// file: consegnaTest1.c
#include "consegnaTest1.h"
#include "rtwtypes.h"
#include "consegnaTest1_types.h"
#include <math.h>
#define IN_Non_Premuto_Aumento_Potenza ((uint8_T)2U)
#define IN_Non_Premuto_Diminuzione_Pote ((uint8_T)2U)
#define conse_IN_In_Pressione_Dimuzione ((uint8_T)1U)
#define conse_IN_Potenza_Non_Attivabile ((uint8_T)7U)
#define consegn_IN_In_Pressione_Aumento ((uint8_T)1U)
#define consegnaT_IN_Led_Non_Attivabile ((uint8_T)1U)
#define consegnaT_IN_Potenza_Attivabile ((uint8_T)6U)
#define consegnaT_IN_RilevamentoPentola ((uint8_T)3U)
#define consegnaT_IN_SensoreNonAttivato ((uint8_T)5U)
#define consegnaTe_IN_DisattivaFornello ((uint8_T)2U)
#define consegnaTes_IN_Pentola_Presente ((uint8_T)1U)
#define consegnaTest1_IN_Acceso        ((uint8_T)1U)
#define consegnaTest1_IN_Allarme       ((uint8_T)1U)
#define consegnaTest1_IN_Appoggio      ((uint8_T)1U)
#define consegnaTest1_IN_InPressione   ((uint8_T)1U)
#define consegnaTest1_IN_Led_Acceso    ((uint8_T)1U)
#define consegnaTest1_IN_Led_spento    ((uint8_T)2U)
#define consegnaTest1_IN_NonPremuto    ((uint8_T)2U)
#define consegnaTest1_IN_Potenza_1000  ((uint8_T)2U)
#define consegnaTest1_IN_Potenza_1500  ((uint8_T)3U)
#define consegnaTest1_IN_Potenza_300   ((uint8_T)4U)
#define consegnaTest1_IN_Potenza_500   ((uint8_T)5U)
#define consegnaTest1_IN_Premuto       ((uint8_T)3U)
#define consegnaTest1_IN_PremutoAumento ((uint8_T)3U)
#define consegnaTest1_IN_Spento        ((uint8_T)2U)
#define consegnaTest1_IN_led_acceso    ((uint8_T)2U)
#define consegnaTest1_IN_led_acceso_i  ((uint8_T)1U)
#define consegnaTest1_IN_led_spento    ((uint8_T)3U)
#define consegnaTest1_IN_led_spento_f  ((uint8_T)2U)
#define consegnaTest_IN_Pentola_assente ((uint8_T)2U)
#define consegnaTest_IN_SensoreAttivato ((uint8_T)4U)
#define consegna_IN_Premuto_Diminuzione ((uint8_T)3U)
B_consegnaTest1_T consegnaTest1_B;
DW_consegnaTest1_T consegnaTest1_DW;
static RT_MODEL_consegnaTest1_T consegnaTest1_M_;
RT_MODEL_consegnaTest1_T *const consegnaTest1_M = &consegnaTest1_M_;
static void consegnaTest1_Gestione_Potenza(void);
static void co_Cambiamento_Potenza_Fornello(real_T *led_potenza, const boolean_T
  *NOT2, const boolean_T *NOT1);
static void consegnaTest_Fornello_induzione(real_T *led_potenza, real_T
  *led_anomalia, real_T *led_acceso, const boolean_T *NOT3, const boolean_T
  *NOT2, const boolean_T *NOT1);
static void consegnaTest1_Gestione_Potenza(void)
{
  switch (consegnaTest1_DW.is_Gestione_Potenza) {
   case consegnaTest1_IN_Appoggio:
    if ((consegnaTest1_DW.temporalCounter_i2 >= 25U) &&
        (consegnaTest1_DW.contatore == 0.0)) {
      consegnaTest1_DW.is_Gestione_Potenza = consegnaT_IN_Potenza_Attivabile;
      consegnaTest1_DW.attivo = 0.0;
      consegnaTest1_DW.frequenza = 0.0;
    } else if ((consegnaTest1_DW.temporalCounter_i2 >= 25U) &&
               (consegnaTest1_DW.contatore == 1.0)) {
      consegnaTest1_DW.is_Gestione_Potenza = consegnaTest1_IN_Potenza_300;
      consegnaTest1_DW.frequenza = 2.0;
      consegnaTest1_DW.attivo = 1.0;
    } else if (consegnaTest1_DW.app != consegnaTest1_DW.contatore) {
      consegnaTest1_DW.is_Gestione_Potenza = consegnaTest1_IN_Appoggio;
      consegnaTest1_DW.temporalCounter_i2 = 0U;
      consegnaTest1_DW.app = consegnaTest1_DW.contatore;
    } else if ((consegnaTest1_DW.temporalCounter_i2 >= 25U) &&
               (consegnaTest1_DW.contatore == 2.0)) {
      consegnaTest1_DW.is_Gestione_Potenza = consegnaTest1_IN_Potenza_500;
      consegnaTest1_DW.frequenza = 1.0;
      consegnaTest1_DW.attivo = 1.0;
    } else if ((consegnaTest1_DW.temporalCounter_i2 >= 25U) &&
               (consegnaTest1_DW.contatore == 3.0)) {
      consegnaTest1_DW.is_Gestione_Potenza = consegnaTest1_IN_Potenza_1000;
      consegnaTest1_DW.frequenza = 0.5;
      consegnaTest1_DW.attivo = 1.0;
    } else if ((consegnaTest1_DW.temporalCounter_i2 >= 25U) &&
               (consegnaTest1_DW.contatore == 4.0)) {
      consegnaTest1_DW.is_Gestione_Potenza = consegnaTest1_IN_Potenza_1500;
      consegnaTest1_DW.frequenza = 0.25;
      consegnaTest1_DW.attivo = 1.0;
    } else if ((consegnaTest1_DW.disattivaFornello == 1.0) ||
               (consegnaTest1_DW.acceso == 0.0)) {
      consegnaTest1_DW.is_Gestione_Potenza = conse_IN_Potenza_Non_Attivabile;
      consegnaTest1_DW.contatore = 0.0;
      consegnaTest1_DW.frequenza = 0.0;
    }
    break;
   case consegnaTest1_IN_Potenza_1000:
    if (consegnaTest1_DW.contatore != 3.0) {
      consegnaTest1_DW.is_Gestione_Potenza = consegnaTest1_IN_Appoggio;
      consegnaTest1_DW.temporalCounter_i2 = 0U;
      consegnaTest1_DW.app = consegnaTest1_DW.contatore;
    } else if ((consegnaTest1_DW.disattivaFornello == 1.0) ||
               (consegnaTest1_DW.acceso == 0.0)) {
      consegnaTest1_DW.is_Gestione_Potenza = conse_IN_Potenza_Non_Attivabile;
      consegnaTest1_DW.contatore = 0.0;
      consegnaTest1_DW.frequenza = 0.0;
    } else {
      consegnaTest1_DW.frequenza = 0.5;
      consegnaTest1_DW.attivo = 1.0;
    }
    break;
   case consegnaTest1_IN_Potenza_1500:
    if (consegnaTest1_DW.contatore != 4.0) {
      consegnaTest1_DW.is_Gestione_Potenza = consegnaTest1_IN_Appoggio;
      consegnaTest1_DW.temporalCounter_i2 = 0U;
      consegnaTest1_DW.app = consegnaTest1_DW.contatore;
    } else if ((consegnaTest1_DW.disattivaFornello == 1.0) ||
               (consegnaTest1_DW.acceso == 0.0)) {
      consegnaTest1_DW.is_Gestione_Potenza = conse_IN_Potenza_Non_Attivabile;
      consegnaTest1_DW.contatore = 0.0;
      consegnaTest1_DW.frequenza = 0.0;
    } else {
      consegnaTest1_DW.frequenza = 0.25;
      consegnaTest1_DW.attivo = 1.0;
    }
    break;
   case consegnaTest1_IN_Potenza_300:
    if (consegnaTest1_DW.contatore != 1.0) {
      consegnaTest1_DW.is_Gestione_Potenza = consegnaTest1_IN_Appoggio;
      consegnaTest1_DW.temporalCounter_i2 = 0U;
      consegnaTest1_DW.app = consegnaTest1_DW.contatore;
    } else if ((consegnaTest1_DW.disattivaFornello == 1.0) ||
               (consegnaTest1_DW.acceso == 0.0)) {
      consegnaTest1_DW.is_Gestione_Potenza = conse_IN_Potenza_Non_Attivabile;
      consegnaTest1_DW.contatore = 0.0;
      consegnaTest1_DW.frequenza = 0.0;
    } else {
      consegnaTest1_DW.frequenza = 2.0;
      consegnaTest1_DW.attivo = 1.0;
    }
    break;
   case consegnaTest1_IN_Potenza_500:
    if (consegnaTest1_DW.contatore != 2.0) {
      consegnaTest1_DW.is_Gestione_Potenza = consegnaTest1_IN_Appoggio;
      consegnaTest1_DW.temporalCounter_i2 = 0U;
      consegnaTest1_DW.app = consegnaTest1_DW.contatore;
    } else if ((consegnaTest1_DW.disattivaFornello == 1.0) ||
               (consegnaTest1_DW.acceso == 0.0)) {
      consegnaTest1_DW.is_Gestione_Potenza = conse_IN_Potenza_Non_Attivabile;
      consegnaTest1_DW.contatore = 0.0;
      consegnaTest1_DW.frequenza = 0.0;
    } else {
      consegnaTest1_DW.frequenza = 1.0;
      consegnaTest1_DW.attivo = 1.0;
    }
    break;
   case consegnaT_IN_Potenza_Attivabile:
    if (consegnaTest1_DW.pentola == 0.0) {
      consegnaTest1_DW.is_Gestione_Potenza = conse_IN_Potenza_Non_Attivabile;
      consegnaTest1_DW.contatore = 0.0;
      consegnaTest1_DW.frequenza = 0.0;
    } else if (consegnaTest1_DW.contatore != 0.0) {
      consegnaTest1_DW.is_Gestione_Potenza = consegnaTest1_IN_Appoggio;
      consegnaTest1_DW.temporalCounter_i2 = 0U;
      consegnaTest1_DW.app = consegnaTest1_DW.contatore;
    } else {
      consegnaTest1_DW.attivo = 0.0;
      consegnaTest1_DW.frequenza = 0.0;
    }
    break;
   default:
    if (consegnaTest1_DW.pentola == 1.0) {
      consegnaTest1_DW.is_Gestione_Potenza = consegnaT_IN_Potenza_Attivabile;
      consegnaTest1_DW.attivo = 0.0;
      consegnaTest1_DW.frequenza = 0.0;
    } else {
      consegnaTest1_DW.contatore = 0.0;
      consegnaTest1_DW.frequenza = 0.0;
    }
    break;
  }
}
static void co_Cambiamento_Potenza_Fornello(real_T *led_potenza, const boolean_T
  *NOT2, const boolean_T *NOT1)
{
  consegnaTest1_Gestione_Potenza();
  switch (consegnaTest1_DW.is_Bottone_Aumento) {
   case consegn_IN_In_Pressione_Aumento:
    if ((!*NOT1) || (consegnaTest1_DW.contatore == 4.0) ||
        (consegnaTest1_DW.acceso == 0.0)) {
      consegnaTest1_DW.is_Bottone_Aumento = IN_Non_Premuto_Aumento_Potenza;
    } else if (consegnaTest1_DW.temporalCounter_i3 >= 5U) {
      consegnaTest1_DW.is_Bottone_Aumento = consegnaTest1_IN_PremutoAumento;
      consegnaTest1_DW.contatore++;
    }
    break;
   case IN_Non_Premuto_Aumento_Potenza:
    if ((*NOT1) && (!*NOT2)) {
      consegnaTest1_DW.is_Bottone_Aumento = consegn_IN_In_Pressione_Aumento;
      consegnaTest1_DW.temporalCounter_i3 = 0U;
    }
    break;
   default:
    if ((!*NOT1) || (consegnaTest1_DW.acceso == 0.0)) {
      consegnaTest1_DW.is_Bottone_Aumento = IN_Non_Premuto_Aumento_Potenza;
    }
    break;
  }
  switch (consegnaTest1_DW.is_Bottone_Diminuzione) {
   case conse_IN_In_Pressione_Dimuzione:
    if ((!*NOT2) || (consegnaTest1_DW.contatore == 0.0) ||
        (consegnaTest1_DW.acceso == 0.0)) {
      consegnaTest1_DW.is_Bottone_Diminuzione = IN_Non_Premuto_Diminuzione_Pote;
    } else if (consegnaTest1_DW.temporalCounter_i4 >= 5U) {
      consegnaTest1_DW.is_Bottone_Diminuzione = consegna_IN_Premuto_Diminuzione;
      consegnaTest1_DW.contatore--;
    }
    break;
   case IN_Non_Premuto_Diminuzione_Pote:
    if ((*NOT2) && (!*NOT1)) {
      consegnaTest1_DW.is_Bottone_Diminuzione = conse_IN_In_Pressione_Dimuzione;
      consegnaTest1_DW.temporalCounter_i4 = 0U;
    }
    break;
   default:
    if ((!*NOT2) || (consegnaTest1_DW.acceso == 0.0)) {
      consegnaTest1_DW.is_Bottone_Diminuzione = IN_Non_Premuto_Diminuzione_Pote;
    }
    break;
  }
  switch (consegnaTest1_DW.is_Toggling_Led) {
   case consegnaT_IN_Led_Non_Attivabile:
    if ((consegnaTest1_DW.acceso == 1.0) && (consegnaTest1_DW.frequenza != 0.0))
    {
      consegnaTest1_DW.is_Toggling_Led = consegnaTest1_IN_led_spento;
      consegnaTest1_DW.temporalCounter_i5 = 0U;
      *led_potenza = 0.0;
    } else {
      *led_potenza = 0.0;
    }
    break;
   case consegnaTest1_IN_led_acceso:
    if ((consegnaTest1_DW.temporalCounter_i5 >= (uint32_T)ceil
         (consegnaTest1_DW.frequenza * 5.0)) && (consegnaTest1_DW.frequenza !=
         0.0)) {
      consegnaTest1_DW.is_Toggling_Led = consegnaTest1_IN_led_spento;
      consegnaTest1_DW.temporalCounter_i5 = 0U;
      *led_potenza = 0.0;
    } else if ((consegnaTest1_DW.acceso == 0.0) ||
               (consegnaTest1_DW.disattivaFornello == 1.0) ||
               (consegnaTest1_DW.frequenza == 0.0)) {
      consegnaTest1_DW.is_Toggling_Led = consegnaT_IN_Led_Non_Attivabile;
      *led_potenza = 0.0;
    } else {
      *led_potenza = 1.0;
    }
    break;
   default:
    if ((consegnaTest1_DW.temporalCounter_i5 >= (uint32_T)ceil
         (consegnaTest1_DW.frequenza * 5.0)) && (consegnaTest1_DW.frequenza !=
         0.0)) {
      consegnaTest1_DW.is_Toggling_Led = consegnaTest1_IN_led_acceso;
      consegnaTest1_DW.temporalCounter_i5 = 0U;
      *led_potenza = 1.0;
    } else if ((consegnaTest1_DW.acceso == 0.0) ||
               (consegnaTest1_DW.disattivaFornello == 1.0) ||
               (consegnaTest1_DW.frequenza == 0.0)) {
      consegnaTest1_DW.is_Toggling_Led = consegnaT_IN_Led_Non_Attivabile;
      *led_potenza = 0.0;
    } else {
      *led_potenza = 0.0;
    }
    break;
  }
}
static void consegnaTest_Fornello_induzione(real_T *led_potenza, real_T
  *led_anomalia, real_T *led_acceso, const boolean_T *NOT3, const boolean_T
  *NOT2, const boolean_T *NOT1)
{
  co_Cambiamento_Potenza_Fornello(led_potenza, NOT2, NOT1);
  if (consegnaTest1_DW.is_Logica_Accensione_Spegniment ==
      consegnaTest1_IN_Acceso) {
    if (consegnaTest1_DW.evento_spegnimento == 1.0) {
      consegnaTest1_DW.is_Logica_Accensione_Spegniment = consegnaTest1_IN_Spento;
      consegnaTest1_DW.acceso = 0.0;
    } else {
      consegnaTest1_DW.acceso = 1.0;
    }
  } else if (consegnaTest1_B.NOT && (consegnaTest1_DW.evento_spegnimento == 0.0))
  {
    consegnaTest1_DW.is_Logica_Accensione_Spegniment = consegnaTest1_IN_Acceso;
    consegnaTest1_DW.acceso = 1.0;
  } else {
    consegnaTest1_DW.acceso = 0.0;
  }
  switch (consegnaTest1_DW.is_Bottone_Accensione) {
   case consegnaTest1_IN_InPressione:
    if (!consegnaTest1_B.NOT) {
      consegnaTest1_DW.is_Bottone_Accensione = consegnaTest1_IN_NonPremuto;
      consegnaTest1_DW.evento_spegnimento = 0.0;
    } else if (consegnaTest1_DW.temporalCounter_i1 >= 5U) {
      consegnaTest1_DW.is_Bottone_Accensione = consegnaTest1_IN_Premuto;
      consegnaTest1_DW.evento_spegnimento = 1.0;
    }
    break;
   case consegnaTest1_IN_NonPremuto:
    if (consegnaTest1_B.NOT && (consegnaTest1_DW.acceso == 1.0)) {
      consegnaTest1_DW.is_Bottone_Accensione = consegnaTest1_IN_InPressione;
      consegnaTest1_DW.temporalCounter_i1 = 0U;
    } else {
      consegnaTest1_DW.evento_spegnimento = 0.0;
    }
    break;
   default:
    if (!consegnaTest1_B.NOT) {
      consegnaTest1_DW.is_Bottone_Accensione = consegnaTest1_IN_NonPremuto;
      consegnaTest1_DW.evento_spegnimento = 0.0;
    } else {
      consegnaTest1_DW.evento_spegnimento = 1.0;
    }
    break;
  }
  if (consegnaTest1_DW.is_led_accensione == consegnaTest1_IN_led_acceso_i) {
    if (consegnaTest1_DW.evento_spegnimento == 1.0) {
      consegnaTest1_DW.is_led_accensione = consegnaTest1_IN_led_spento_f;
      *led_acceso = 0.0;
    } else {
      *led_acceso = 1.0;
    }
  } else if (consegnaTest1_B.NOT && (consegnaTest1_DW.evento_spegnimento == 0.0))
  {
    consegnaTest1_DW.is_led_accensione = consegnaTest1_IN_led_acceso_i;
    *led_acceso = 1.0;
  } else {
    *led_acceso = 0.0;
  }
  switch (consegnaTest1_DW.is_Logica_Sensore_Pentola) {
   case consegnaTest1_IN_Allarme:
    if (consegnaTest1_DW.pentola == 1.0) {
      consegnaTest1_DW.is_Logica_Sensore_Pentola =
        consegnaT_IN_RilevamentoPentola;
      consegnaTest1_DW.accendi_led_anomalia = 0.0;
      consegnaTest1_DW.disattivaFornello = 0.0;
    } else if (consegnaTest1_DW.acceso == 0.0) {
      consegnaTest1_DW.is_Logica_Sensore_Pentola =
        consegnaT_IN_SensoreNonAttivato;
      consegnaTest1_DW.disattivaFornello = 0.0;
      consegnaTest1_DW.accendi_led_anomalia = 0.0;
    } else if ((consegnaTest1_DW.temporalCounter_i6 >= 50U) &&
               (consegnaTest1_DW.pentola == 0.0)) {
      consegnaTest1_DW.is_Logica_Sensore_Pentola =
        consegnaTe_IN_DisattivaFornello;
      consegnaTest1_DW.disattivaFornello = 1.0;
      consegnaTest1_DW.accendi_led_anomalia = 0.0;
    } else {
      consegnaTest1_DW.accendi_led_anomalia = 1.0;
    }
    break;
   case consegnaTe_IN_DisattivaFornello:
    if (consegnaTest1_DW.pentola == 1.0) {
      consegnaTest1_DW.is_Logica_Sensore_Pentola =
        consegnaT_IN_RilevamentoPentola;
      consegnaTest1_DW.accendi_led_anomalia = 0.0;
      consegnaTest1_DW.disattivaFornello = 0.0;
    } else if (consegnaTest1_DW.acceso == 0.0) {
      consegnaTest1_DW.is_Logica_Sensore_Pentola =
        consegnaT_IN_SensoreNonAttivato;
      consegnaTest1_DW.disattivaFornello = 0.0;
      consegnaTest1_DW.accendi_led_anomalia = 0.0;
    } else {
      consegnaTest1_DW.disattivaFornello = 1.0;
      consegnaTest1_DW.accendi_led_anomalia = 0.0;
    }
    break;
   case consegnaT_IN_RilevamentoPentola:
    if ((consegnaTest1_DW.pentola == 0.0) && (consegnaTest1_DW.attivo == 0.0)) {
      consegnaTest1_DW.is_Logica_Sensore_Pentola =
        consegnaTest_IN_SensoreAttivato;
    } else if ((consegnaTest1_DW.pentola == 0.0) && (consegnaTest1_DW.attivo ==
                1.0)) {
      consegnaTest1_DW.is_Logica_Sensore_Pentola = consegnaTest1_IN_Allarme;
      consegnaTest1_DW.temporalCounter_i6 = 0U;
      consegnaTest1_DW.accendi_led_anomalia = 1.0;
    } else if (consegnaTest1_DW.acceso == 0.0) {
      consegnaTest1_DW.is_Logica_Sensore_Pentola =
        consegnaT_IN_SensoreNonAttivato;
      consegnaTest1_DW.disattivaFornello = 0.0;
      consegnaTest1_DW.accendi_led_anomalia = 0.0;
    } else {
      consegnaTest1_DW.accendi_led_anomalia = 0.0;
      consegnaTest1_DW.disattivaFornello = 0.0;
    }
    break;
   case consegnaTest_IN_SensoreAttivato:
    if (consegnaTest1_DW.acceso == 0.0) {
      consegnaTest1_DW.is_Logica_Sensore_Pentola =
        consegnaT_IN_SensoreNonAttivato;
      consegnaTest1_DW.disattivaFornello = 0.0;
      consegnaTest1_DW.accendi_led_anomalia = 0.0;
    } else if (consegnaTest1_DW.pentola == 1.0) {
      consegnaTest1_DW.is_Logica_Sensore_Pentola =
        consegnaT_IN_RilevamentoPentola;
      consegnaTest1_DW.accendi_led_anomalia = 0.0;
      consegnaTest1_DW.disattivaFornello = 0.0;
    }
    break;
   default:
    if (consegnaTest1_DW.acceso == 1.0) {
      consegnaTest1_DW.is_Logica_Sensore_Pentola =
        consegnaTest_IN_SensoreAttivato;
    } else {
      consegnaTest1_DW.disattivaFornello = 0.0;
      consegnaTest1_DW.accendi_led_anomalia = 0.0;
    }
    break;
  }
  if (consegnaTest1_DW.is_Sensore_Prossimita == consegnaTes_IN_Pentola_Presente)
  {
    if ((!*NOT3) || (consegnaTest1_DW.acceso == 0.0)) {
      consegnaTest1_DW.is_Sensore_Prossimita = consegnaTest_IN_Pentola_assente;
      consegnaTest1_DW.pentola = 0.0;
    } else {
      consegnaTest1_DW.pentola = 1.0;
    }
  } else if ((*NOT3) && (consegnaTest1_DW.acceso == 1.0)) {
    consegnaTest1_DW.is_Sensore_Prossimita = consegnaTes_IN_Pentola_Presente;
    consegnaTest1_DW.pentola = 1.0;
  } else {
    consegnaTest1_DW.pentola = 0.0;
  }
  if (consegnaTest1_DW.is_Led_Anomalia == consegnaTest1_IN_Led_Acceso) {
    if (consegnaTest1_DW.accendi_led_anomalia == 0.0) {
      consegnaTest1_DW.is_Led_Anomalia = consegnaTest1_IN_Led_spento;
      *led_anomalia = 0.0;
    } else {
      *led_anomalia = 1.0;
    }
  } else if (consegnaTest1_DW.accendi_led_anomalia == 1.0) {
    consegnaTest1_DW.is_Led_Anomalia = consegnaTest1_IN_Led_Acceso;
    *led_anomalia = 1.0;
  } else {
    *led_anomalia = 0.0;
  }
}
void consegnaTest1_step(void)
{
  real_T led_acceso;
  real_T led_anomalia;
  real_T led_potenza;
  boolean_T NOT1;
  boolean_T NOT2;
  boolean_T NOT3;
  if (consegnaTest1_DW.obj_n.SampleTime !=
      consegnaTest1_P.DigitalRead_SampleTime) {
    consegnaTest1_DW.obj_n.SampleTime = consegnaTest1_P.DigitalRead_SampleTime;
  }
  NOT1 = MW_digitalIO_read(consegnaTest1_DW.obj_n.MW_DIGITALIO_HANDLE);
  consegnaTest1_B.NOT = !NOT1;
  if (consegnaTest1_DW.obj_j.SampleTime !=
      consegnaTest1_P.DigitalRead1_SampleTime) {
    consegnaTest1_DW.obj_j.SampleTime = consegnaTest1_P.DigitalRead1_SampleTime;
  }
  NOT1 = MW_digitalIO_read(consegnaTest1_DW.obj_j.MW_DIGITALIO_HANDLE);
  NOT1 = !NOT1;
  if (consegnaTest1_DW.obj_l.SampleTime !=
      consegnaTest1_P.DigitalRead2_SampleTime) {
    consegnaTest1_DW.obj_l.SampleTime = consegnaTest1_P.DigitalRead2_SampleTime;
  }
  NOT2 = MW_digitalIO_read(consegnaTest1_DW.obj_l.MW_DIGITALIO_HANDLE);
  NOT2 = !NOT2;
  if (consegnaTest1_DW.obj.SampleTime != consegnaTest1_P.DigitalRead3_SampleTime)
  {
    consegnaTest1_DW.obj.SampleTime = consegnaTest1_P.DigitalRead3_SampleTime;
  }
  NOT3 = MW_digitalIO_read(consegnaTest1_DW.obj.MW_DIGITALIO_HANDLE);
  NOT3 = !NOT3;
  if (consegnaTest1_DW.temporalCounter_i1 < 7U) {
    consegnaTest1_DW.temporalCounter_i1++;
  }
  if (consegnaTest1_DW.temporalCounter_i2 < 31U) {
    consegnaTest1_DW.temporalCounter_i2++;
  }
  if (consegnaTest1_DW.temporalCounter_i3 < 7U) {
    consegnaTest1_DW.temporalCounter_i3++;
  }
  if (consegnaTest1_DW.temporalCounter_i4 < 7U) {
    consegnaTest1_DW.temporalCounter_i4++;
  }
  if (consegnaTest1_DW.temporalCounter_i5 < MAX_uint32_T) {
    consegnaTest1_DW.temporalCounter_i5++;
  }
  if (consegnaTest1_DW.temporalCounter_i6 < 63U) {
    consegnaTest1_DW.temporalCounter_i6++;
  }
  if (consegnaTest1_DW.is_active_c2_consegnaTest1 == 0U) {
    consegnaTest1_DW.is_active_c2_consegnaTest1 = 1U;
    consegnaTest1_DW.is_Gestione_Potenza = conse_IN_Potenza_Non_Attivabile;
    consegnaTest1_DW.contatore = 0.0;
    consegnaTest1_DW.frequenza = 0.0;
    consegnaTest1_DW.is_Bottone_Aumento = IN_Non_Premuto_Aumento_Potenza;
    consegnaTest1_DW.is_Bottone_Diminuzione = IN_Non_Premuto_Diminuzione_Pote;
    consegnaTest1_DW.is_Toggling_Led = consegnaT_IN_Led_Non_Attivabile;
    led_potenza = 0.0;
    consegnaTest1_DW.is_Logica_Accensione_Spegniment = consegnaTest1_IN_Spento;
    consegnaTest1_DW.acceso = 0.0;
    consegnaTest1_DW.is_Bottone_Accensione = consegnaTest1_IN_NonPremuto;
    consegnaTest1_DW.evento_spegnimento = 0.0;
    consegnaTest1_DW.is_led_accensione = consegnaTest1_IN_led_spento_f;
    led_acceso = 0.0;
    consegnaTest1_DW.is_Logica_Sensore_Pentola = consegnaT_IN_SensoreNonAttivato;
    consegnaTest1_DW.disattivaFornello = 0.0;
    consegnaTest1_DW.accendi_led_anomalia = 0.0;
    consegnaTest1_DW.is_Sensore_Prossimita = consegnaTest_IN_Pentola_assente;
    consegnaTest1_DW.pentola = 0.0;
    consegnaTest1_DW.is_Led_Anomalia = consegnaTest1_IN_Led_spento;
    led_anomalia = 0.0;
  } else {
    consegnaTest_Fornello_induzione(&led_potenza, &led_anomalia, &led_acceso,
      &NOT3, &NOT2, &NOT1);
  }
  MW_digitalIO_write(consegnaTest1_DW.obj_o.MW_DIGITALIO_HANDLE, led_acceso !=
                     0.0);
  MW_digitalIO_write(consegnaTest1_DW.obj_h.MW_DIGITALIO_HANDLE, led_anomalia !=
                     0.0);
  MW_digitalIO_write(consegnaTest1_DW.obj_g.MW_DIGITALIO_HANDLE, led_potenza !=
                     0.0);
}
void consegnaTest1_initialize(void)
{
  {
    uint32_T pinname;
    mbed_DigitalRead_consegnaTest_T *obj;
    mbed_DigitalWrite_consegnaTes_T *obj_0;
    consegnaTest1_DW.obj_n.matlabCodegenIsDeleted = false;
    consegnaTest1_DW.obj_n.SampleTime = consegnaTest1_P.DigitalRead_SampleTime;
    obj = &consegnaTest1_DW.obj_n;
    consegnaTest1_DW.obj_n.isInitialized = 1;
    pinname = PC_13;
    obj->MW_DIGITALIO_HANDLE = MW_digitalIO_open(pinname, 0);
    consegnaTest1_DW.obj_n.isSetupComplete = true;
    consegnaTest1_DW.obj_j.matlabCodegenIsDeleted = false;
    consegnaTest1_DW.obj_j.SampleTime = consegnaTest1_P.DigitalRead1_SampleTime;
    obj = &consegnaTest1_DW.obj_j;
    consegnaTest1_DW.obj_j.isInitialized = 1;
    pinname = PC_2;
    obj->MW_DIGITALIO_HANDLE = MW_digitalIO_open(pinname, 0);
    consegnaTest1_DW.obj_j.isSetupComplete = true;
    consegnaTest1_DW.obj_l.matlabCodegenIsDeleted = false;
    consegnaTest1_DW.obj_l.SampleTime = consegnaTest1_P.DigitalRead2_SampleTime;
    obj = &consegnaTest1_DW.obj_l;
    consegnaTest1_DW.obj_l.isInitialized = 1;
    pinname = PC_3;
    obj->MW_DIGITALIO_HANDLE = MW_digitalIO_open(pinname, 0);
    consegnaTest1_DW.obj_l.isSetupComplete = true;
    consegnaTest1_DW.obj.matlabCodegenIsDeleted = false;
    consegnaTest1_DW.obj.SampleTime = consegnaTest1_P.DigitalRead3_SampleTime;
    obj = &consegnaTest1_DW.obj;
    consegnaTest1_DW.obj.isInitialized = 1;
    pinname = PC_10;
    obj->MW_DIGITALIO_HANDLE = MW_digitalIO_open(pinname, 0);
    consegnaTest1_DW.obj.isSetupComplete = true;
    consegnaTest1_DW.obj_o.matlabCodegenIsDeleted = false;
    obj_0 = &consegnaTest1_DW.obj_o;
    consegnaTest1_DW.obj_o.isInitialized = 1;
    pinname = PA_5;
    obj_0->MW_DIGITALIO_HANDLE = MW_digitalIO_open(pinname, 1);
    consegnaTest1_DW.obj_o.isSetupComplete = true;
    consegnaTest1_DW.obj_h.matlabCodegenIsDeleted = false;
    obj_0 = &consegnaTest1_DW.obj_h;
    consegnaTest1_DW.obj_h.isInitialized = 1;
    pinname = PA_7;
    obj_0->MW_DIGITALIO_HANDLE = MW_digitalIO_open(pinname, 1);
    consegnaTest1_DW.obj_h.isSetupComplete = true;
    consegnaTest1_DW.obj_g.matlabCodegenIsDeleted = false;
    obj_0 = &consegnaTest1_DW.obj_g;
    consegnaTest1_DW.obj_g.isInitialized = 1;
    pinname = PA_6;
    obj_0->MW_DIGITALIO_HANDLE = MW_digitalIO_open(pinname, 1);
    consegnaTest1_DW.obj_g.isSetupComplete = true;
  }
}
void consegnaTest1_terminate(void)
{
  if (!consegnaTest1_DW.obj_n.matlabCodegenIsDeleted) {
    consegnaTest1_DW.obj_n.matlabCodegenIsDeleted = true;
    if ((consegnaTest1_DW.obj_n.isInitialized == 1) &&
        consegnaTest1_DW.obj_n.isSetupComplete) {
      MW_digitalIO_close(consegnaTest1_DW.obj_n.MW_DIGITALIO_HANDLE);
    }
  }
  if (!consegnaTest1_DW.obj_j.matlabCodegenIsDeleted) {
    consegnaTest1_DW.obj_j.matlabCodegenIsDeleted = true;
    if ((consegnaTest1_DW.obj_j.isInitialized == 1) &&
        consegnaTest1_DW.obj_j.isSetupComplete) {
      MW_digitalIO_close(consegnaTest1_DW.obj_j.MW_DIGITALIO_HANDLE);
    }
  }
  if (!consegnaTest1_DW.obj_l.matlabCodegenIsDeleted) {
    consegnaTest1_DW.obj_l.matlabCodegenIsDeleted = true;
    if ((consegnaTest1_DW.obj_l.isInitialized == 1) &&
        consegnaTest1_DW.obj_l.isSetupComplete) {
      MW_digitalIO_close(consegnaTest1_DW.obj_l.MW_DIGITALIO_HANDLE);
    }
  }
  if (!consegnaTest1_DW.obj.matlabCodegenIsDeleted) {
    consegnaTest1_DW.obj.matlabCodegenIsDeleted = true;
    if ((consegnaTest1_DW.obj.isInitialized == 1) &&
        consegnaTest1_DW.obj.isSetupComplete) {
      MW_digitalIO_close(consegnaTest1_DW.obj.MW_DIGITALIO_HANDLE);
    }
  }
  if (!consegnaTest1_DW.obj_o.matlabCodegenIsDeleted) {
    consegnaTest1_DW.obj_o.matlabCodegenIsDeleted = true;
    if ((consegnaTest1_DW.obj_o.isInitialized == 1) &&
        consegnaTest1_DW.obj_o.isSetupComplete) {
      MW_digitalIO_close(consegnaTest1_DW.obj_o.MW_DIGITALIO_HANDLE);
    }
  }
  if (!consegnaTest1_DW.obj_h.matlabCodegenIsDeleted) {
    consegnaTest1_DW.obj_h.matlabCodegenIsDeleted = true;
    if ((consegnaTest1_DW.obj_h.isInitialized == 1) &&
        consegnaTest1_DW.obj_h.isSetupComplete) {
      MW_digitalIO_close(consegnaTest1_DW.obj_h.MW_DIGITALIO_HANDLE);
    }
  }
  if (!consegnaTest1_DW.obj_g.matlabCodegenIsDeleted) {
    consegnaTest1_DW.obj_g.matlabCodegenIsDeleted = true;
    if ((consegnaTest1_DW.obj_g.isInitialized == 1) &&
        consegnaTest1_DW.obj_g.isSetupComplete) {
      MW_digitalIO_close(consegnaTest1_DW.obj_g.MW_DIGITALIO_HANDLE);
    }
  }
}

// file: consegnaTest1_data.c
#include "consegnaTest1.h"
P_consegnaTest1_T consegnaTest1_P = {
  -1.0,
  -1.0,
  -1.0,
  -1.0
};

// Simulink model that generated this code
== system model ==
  DigitalWrite : mbedblockslib/Digital Write  <- 1: Stateflowchart#1
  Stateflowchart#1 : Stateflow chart  <- 1: NOT, 2: NOT1, 3: NOT2, 4: NOT3
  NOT : Logic  Operator=NOT  <- 1: DigitalRead
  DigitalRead : mbedblockslib/Digital Read
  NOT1 : Logic  Operator=NOT  <- 1: DigitalRead1
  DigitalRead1 : mbedblockslib/Digital Read
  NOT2 : Logic  Operator=NOT  <- 1: DigitalRead2
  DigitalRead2 : mbedblockslib/Digital Read
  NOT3 : Logic  Operator=NOT  <- 1: DigitalRead3
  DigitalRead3 : mbedblockslib/Digital Read
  DigitalWrite#1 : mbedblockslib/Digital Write  <- 1: Stateflowchart#1/3
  DigitalWrite#2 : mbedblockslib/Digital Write  <- 1: Stateflowchart#1/2
== stateflow chart Stateflowchart#1 ==
  state Fornello_induzione
    state Accensione [parallel]
      settings: executionOrder=2
      state led_accensione [parallel]
        settings: executionOrder=3
        state led_acceso
          led_acceso=1;
        state led_spento
          led_acceso = 0;
        (default) -> Fornello_induzione.Accensione.led_accensione.led_spento
        Fornello_induzione.Accensione.led_accensione.led_acceso -> Fornello_induzione.Accensione.led_accensione.led_spento : [evento_spegnimento == 1]
        Fornello_induzione.Accensione.led_accensione.led_spento -> Fornello_induzione.Accensione.led_accensione.led_acceso : [bottone_accensione == 1 && evento_spegnimento == 0]
      state Logica_Accensione_Spegnimento [parallel]
        settings: executionOrder=1
        state Acceso
          acceso = 1;
        state Spento
          acceso = 0;
        (default) -> Spento
        Acceso -> Spento : [evento_spegnimento == 1]
        Spento -> Acceso : [bottone_accensione == 1 && evento_spegnimento == 0]
      state Bottone_Accensione [parallel]
        settings: executionOrder=2
        state NonPremuto
          evento_spegnimento = 0;
        state InPressione
        state Premuto
          evento_spegnimento = 1;
        (default) -> NonPremuto
        InPressione -> Premuto [order 2] : [after(1,sec)]
        NonPremuto -> InPressione : [bottone_accensione == 1 && acceso == 1]
        InPressione -> NonPremuto [order 1] : [bottone_accensione == 0]
        Premuto -> NonPremuto : [bottone_accensione == 0]
      (default) -> led_accensione [order 3]
      (default) -> Logica_Accensione_Spegnimento [order 1]
      (default) -> Bottone_Accensione [order 2]
    state Cambiamento_Potenza_Fornello [parallel]
      settings: executionOrder=1
      state Gestione_Potenza [parallel]
        settings: executionOrder=1
        state Potenza_300
          potenza=300;
          frequenza=2;
          attivo = 1;
        state Potenza_500
          potenza=500;
          frequenza=1;
          attivo = 1;
        state Appoggio
          en: app = contatore;
        state Potenza_Attivabile
          potenza = 0;
          attivo = 0;
          frequenza = 0;
        state Potenza_Non_Attivabile
          contatore = 0;
          potenza = 0;
          frequenza = 0;
        state Potenza_1000
          potenza=1000;
          frequenza=0.5;
          attivo = 1;
        state Potenza_1500
          potenza=1500;
          frequenza=0.25;
          attivo = 1;
        Potenza_500 -> Potenza_Non_Attivabile [order 2] : [disattivaFornello == 1 || acceso == 0]
        Potenza_300 -> Potenza_Non_Attivabile [order 2] : [disattivaFornello == 1 || acceso == 0]
        Appoggio -> Potenza_300 [order 2] : [after(5,sec) && contatore == 1]
        Potenza_300 -> Appoggio [order 1] : [contatore ~= 1]
        Appoggio -> Potenza_500 [order 4] : [after(5,sec) && contatore == 2]
        Potenza_500 -> Appoggio [order 1] : [contatore ~= 2]
        Appoggio -> Appoggio [order 3] : [app ~= contatore]
        (default) -> Potenza_Non_Attivabile
        Potenza_Non_Attivabile -> Potenza_Attivabile : [pentola == 1]
        Potenza_Attivabile -> Appoggio [order 2] : [contatore ~= 0]
        Potenza_Attivabile -> Potenza_Non_Attivabile [order 1] : [pentola == 0]
        Appoggio -> Potenza_Attivabile [order 1] : [after(5,sec) && contatore == 0]
        Appoggio -> Potenza_1000 [order 5] : [after(5,sec) && contatore == 3]
        Potenza_1000 -> Appoggio [order 1] : [contatore ~= 3]
        Potenza_1000 -> Potenza_Non_Attivabile [order 2] : [disattivaFornello == 1 || acceso == 0]
        Potenza_1500 -> Potenza_Non_Attivabile [order 2] : [disattivaFornello == 1 || acceso == 0]
        Appoggio -> Potenza_Non_Attivabile [order 7] : [disattivaFornello == 1 || acceso == 0 ]
        Potenza_1500 -> Appoggio [order 1] : [contatore ~= 4]
        Appoggio -> Potenza_1500 [order 6] : [after(5,sec) && contatore == 4]
      state Bottone_Aumento [parallel]
        settings: executionOrder=2
        state Non_Premuto_Aumento_Potenza
        state In_Pressione_Aumento
        state PremutoAumento
          en: contatore = contatore + 1;
        (default) -> Non_Premuto_Aumento_Potenza
        In_Pressione_Aumento -> PremutoAumento [order 2] : [after(1,sec)]
        Non_Premuto_Aumento_Potenza -> In_Pressione_Aumento : [bottone_aumento == 1 && bottone_diminuzione == 0]
        In_Pressione_Aumento -> Non_Premuto_Aumento_Potenza [order 1] : [bottone_aumento == 0 || contatore == 4 || acceso == 0]
        PremutoAumento -> Non_Premuto_Aumento_Potenza : [bottone_aumento == 0 || acceso == 0]
      state Bottone_Diminuzione [parallel]
        settings: executionOrder=3
        state Non_Premuto_Diminuzione_Potenza
        state In_Pressione_Dimuzione
        state Premuto_Diminuzione
          en: contatore = contatore - 1;
        (default) -> Non_Premuto_Diminuzione_Potenza
        In_Pressione_Dimuzione -> Premuto_Diminuzione [order 2] : [after(1,sec)]
        Non_Premuto_Diminuzione_Potenza -> In_Pressione_Dimuzione : [bottone_diminuzione == 1 && bottone_aumento == 0]
        In_Pressione_Dimuzione -> Non_Premuto_Diminuzione_Potenza [order 1] : [bottone_diminuzione == 0 || contatore == 0 || acceso == 0]
        Premuto_Diminuzione -> Non_Premuto_Diminuzione_Potenza : [bottone_diminuzione == 0 || acceso == 0]
      state Toggling_Led [parallel]
        settings: executionOrder=4
        state led_spento
          led_potenza = 0;
        state Led_Non_Attivabile
          led_potenza = 0;
        state led_acceso
          led_potenza = 1;
        Led_Non_Attivabile -> Fornello_induzione.Cambiamento_Potenza_Fornello.Toggling_Led.led_spento : [acceso == 1 && frequenza ~= 0 ]
        (default) -> Led_Non_Attivabile
        Fornello_induzione.Cambiamento_Potenza_Fornello.Toggling_Led.led_spento -> Led_Non_Attivabile [order 2] : [acceso == 0 || disattivaFornello == 1 || frequenza ==0 ]
        Fornello_induzione.Cambiamento_Potenza_Fornello.Toggling_Led.led_spento -> Fornello_induzione.Cambiamento_Potenza_Fornello.Toggling_Led.led_acceso [order 1] : [after(frequenza,sec) && frequenza ~= 0]
        Fornello_induzione.Cambiamento_Potenza_Fornello.Toggling_Led.led_acceso -> Fornello_induzione.Cambiamento_Potenza_Fornello.Toggling_Led.led_spento [order 1] : [after(frequenza, sec) && frequenza ~= 0]
        Fornello_induzione.Cambiamento_Potenza_Fornello.Toggling_Led.led_acceso -> Led_Non_Attivabile [order 2] : [acceso == 0 || disattivaFornello == 1 || frequenza == 0]
      (default) -> Gestione_Potenza [order 4]
      (default) -> Bottone_Aumento [order 1]
      (default) -> Bottone_Diminuzione [order 2]
      (default) -> Toggling_Led [order 3]
    state Prossimita_Pentola [parallel]
      settings: executionOrder=3
      state Logica_Sensore_Pentola [parallel]
        settings: executionOrder=1
        state SensoreNonAttivato
          disattivaFornello = 0;
          accendi_led_anomalia = 0;
          pentola = 0;
        state SensoreAttivato
          anomalia = 0;
        state RilevamentoPentola
          accendi_led_anomalia = 0;
          disattivaFornello = 0;
        state DisattivaFornello
          disattivaFornello = 1;
          accendi_led_anomalia = 0;
          pentola = 0;
        state Allarme
          accendi_led_anomalia = 1;
        RilevamentoPentola -> SensoreNonAttivato [order 3] : [acceso == 0]
        (default) -> SensoreNonAttivato
        SensoreAttivato -> RilevamentoPentola [order 2] : [pentola == 1]
        SensoreNonAttivato -> SensoreAttivato : [acceso == 1]
        SensoreAttivato -> SensoreNonAttivato [order 1] : [acceso == 0]
        RilevamentoPentola -> SensoreAttivato [order 1] : [pentola == 0 && attivo == 0]
        Allarme -> SensoreNonAttivato [order 2] : [acceso == 0]
        DisattivaFornello -> SensoreNonAttivato [order 2] : [acceso == 0]
        DisattivaFornello -> RilevamentoPentola [order 1] : [pentola == 1]
        Allarme -> RilevamentoPentola [order 1] : [pentola == 1]
        RilevamentoPentola -> Allarme [order 2] : [pentola == 0 && attivo == 1]
        Allarme -> DisattivaFornello [order 3] : [after(10,sec) && pentola == 0]
      state Sensore_Prossimita [parallel]
        settings: executionOrder=2
        state Pentola_assente
          pentola = 0;
        state Pentola_Presente
          pentola = 1;
        (default) -> Pentola_assente
        Pentola_assente -> Pentola_Presente : [sensore_prox == 1 && acceso == 1]
        Pentola_Presente -> Pentola_assente : [sensore_prox == 0 || acceso == 0]
      state Led_Anomalia [parallel]
        settings: executionOrder=3
        state Led_spento
          led_anomalia = 0;
        state Led_Acceso
          led_anomalia = 1;
        (default) -> Led_spento
        Led_spento -> Led_Acceso : [accendi_led_anomalia == 1]
        Led_Acceso -> Led_spento : [accendi_led_anomalia == 0]
      (default) -> Logica_Sensore_Pentola [order 1]
      (default) -> Sensore_Prossimita [order 2]
      (default) -> Led_Anomalia [order 3]
    (default) -> Accensione [order 1]
    (default) -> Cambiamento_Potenza_Fornello [order 3]
    (default) -> Prossimita_Pentola [order 2]
  (default) -> Fornello_induzione
  data: bottone_accensione input; bottone_aumento input; bottone_diminuzione input; sensore_prox input; acceso local; app local; attivo local; contatore local; disattivaFornello local; evento_spegnimento local; pentola local; anomalia local; led_acceso output; potenza local; led_potenza output; frequenza local =0; accendi_led_anomalia local; led_anomalia output
